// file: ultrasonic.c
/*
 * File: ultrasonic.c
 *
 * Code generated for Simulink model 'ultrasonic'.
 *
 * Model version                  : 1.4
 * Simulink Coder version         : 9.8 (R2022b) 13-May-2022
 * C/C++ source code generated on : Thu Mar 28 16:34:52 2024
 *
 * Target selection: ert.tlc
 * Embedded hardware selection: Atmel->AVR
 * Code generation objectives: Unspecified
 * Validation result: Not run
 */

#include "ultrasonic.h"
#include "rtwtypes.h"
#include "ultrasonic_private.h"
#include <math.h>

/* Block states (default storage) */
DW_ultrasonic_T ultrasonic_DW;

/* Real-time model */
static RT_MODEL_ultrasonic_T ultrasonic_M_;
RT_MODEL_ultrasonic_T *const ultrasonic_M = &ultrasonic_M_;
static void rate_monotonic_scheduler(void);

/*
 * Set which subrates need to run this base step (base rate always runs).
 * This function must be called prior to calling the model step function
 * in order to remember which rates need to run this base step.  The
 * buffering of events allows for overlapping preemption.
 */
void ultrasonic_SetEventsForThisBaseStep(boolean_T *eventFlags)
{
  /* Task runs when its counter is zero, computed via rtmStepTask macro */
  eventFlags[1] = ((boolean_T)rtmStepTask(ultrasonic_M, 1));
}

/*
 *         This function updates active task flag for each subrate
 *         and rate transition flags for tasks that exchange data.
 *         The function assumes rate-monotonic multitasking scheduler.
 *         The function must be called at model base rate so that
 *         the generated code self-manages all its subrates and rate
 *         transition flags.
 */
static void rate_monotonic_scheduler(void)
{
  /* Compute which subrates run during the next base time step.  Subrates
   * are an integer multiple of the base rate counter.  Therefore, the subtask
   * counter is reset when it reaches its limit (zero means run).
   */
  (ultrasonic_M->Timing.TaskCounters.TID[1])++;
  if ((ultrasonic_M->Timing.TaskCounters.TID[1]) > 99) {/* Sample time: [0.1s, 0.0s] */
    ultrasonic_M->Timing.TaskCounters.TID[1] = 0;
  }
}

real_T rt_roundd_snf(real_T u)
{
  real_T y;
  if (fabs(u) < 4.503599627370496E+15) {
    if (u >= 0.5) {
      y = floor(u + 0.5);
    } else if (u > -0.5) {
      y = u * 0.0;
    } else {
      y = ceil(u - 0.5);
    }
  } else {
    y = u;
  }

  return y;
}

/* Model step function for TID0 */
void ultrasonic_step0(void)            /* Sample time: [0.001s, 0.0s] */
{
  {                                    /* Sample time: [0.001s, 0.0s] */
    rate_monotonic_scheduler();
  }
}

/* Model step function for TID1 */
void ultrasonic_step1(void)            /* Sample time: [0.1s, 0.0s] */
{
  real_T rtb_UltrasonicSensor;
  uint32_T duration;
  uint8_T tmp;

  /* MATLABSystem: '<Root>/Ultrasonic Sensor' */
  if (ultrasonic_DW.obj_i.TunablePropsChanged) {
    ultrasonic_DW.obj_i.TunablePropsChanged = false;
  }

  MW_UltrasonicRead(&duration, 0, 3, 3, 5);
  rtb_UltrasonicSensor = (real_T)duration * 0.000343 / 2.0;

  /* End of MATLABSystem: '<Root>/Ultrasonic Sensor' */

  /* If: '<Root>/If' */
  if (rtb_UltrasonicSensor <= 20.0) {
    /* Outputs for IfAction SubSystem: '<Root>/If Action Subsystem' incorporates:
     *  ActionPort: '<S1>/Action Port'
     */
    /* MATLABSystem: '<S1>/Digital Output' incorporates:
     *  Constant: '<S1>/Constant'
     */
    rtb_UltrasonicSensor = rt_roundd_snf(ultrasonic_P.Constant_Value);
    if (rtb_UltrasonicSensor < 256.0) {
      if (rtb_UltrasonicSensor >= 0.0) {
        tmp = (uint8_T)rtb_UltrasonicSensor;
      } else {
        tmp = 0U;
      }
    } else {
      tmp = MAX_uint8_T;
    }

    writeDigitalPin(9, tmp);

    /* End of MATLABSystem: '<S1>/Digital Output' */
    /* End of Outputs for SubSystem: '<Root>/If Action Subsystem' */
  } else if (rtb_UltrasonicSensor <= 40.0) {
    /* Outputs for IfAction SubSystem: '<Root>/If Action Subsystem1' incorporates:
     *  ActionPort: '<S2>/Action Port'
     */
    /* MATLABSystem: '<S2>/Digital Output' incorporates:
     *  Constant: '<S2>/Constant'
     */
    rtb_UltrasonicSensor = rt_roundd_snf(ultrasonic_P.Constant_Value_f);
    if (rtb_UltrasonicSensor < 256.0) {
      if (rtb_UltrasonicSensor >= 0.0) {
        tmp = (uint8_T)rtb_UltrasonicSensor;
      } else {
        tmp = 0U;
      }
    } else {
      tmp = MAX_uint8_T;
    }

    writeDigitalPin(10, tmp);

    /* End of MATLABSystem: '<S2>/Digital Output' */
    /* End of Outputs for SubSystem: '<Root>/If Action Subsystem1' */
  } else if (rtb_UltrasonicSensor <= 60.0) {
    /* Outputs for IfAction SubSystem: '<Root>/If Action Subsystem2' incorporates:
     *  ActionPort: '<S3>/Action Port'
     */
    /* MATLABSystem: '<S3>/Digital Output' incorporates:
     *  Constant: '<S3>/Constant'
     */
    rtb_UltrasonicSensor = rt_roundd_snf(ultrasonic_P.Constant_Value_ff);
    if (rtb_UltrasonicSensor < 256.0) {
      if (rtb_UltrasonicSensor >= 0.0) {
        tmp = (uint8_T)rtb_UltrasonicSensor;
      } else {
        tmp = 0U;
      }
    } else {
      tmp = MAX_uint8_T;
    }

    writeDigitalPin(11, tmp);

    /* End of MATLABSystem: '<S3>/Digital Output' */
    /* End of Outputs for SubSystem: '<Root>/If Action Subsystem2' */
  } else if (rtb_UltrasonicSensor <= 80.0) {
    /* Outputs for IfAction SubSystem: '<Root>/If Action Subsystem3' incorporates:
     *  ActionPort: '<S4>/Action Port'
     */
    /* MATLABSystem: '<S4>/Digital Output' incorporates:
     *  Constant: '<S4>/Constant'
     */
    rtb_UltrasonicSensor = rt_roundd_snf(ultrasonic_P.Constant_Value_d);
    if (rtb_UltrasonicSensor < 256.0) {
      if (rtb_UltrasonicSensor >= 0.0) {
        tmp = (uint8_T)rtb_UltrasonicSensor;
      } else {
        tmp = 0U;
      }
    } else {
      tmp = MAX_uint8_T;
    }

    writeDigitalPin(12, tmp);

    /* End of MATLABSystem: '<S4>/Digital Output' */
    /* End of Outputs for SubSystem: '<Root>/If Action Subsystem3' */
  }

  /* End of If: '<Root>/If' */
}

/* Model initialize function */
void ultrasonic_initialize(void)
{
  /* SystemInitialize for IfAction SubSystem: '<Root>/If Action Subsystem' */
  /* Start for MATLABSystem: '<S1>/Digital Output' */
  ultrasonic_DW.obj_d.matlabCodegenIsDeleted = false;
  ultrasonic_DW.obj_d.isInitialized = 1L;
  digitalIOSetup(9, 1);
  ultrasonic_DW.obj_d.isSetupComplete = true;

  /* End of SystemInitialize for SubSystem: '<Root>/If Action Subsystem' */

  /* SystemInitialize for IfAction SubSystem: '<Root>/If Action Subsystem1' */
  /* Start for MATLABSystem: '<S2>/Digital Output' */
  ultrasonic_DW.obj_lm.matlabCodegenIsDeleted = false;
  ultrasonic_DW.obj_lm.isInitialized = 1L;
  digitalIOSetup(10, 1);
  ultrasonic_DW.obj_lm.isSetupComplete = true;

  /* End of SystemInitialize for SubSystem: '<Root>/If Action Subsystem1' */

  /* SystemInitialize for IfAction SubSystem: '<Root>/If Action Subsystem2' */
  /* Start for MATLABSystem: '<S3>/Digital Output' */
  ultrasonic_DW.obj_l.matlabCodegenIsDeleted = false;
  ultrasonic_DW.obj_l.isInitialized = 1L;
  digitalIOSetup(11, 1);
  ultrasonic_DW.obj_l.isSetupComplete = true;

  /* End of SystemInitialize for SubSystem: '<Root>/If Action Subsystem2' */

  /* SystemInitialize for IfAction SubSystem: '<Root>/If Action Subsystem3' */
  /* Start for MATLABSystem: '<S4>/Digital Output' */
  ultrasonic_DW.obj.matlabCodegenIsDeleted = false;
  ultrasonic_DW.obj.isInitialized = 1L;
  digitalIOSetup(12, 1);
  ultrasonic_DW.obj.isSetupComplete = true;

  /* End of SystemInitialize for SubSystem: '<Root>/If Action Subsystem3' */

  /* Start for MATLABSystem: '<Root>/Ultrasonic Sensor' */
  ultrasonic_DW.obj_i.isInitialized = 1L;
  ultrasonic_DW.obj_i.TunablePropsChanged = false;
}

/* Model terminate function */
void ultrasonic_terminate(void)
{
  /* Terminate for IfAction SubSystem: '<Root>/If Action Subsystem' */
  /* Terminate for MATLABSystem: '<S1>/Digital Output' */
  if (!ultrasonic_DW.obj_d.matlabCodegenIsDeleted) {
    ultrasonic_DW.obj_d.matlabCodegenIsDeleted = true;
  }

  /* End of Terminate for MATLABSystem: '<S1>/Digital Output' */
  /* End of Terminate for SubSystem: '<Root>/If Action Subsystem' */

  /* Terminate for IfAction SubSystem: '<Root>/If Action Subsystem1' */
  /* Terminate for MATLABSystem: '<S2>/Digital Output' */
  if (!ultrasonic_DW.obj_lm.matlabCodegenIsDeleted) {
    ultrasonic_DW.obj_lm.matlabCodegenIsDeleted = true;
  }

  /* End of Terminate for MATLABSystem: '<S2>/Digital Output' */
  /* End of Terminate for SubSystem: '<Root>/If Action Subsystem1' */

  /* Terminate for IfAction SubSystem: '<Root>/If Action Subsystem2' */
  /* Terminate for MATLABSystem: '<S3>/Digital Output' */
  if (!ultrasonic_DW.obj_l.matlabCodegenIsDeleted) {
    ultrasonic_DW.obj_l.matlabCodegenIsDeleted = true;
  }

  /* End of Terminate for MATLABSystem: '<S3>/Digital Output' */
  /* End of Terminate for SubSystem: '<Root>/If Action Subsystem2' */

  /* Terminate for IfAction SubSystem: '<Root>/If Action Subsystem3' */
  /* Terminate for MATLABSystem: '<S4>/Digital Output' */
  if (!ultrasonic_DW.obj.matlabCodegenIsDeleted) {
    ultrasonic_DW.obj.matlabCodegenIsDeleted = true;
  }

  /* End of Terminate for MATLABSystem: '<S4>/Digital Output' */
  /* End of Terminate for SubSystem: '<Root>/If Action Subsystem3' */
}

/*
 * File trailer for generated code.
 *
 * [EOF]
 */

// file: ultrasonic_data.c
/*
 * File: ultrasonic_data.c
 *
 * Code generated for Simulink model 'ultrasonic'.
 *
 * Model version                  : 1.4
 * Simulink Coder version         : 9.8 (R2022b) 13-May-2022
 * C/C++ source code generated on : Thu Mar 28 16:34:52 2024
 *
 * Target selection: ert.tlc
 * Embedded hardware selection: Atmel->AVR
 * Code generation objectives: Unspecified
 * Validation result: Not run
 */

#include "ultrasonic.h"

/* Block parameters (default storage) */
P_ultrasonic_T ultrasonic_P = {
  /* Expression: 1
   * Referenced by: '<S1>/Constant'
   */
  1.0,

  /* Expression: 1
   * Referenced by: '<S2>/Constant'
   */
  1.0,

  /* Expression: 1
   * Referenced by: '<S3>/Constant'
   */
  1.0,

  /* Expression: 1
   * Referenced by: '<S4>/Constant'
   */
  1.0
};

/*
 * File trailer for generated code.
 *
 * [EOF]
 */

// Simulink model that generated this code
simulink model "ultrasonic"  (R2022b)
settings: Solver=FixedStepDiscrete  StartTime=0.0  StopTime=10.0  FixedStep=1e-3  RelTol=1e-3  EnableMultiTasking=on
libraries: arduinolib x4, arduinosensorlib x1

== system ultrasonic ==
  If : If  IfExpression=u1 <= 20  ElseIfExpressions=u1 <= 40,u1 <= 60,u1 <= 80  ShowElse=off
  If Action Subsystem : Subsystem  TreatAsAtomicUnit=on
  If Action Subsystem1 : Subsystem  TreatAsAtomicUnit=on
  If Action Subsystem2 : Subsystem  TreatAsAtomicUnit=on
  If Action Subsystem3 : Subsystem  TreatAsAtomicUnit=on
  Ultrasonic Sensor : arduinosensorlib/Ultrasonic Sensor  NumSignalPins=1  TrigPin=4  EchoPin=5  SignalPin=3  SampleTime_=0.1  blockPlatform=ARDUINO
  wires:
  If/1 -> If Action Subsystem/Action
  If/2 -> If Action Subsystem1/Action
  If/3 -> If Action Subsystem2/Action
  If/4 -> If Action Subsystem3/Action
  Ultrasonic Sensor/1 -> If/1

== system ultrasonic/If Action Subsystem ==
  Action Port : ActionPort  ActionPortLabel=if(u1 <= 20)
  Constant : Constant
  Digital Output : arduinolib/Digital Output  pinNumber=9  Direction=output  blockPlatform=arduino
  wires:
  Constant/1 -> Digital Output/1

== system ultrasonic/If Action Subsystem1 ==
  Action Port : ActionPort  ActionPortLabel=elseif(u1 <= 40)
  Constant : Constant
  Digital Output : arduinolib/Digital Output  pinNumber=10  Direction=output  blockPlatform=arduino
  wires:
  Constant/1 -> Digital Output/1

== system ultrasonic/If Action Subsystem2 ==
  Action Port : ActionPort  ActionPortLabel=elseif(u1 <= 60)
  Constant : Constant
  Digital Output : arduinolib/Digital Output  pinNumber=11  Direction=output  blockPlatform=arduino
  wires:
  Constant/1 -> Digital Output/1

== system ultrasonic/If Action Subsystem3 ==
  Action Port : ActionPort  ActionPortLabel=elseif(u1 <= 80)
  Constant : Constant
  Digital Output : arduinolib/Digital Output  pinNumber=12  Direction=output  blockPlatform=arduino
  wires:
  Constant/1 -> Digital Output/1
